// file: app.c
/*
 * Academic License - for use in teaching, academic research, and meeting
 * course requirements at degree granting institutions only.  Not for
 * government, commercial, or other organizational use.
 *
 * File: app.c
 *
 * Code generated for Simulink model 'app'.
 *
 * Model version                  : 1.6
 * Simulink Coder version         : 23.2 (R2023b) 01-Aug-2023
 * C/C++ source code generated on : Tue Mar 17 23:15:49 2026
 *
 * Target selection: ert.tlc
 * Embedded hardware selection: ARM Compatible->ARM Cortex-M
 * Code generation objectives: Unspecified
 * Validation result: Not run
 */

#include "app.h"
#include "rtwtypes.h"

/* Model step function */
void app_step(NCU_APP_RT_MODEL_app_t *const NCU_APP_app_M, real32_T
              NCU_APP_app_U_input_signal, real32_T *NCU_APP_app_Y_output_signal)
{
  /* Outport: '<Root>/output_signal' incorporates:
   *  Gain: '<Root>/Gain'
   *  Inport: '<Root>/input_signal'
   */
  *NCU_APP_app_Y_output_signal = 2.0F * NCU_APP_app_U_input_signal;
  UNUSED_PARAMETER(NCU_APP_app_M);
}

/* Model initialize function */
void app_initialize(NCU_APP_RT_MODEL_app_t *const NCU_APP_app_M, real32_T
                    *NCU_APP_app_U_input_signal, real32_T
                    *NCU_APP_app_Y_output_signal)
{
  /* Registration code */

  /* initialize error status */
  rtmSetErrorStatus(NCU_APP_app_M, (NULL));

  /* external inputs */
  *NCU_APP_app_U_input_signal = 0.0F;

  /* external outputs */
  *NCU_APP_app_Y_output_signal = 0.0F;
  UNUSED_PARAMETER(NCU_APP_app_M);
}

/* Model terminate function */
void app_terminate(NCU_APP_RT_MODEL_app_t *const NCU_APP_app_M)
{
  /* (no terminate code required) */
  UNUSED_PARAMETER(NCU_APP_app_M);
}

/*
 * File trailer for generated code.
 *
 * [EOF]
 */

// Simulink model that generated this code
simulink model "app"  (R2023b)
settings: Solver=FixedStepDiscrete  StartTime=0.0  StopTime=10.0  FixedStep=0.01  RelTol=1e-3

== system app ==
  input_signal : Inport
  Gain : Gain  Gain=2
  output_signal : Outport  OutDataTypeStr=single
  wires:
  input_signal/1 -> Gain/1
  Gain/1 -> output_signal/1
